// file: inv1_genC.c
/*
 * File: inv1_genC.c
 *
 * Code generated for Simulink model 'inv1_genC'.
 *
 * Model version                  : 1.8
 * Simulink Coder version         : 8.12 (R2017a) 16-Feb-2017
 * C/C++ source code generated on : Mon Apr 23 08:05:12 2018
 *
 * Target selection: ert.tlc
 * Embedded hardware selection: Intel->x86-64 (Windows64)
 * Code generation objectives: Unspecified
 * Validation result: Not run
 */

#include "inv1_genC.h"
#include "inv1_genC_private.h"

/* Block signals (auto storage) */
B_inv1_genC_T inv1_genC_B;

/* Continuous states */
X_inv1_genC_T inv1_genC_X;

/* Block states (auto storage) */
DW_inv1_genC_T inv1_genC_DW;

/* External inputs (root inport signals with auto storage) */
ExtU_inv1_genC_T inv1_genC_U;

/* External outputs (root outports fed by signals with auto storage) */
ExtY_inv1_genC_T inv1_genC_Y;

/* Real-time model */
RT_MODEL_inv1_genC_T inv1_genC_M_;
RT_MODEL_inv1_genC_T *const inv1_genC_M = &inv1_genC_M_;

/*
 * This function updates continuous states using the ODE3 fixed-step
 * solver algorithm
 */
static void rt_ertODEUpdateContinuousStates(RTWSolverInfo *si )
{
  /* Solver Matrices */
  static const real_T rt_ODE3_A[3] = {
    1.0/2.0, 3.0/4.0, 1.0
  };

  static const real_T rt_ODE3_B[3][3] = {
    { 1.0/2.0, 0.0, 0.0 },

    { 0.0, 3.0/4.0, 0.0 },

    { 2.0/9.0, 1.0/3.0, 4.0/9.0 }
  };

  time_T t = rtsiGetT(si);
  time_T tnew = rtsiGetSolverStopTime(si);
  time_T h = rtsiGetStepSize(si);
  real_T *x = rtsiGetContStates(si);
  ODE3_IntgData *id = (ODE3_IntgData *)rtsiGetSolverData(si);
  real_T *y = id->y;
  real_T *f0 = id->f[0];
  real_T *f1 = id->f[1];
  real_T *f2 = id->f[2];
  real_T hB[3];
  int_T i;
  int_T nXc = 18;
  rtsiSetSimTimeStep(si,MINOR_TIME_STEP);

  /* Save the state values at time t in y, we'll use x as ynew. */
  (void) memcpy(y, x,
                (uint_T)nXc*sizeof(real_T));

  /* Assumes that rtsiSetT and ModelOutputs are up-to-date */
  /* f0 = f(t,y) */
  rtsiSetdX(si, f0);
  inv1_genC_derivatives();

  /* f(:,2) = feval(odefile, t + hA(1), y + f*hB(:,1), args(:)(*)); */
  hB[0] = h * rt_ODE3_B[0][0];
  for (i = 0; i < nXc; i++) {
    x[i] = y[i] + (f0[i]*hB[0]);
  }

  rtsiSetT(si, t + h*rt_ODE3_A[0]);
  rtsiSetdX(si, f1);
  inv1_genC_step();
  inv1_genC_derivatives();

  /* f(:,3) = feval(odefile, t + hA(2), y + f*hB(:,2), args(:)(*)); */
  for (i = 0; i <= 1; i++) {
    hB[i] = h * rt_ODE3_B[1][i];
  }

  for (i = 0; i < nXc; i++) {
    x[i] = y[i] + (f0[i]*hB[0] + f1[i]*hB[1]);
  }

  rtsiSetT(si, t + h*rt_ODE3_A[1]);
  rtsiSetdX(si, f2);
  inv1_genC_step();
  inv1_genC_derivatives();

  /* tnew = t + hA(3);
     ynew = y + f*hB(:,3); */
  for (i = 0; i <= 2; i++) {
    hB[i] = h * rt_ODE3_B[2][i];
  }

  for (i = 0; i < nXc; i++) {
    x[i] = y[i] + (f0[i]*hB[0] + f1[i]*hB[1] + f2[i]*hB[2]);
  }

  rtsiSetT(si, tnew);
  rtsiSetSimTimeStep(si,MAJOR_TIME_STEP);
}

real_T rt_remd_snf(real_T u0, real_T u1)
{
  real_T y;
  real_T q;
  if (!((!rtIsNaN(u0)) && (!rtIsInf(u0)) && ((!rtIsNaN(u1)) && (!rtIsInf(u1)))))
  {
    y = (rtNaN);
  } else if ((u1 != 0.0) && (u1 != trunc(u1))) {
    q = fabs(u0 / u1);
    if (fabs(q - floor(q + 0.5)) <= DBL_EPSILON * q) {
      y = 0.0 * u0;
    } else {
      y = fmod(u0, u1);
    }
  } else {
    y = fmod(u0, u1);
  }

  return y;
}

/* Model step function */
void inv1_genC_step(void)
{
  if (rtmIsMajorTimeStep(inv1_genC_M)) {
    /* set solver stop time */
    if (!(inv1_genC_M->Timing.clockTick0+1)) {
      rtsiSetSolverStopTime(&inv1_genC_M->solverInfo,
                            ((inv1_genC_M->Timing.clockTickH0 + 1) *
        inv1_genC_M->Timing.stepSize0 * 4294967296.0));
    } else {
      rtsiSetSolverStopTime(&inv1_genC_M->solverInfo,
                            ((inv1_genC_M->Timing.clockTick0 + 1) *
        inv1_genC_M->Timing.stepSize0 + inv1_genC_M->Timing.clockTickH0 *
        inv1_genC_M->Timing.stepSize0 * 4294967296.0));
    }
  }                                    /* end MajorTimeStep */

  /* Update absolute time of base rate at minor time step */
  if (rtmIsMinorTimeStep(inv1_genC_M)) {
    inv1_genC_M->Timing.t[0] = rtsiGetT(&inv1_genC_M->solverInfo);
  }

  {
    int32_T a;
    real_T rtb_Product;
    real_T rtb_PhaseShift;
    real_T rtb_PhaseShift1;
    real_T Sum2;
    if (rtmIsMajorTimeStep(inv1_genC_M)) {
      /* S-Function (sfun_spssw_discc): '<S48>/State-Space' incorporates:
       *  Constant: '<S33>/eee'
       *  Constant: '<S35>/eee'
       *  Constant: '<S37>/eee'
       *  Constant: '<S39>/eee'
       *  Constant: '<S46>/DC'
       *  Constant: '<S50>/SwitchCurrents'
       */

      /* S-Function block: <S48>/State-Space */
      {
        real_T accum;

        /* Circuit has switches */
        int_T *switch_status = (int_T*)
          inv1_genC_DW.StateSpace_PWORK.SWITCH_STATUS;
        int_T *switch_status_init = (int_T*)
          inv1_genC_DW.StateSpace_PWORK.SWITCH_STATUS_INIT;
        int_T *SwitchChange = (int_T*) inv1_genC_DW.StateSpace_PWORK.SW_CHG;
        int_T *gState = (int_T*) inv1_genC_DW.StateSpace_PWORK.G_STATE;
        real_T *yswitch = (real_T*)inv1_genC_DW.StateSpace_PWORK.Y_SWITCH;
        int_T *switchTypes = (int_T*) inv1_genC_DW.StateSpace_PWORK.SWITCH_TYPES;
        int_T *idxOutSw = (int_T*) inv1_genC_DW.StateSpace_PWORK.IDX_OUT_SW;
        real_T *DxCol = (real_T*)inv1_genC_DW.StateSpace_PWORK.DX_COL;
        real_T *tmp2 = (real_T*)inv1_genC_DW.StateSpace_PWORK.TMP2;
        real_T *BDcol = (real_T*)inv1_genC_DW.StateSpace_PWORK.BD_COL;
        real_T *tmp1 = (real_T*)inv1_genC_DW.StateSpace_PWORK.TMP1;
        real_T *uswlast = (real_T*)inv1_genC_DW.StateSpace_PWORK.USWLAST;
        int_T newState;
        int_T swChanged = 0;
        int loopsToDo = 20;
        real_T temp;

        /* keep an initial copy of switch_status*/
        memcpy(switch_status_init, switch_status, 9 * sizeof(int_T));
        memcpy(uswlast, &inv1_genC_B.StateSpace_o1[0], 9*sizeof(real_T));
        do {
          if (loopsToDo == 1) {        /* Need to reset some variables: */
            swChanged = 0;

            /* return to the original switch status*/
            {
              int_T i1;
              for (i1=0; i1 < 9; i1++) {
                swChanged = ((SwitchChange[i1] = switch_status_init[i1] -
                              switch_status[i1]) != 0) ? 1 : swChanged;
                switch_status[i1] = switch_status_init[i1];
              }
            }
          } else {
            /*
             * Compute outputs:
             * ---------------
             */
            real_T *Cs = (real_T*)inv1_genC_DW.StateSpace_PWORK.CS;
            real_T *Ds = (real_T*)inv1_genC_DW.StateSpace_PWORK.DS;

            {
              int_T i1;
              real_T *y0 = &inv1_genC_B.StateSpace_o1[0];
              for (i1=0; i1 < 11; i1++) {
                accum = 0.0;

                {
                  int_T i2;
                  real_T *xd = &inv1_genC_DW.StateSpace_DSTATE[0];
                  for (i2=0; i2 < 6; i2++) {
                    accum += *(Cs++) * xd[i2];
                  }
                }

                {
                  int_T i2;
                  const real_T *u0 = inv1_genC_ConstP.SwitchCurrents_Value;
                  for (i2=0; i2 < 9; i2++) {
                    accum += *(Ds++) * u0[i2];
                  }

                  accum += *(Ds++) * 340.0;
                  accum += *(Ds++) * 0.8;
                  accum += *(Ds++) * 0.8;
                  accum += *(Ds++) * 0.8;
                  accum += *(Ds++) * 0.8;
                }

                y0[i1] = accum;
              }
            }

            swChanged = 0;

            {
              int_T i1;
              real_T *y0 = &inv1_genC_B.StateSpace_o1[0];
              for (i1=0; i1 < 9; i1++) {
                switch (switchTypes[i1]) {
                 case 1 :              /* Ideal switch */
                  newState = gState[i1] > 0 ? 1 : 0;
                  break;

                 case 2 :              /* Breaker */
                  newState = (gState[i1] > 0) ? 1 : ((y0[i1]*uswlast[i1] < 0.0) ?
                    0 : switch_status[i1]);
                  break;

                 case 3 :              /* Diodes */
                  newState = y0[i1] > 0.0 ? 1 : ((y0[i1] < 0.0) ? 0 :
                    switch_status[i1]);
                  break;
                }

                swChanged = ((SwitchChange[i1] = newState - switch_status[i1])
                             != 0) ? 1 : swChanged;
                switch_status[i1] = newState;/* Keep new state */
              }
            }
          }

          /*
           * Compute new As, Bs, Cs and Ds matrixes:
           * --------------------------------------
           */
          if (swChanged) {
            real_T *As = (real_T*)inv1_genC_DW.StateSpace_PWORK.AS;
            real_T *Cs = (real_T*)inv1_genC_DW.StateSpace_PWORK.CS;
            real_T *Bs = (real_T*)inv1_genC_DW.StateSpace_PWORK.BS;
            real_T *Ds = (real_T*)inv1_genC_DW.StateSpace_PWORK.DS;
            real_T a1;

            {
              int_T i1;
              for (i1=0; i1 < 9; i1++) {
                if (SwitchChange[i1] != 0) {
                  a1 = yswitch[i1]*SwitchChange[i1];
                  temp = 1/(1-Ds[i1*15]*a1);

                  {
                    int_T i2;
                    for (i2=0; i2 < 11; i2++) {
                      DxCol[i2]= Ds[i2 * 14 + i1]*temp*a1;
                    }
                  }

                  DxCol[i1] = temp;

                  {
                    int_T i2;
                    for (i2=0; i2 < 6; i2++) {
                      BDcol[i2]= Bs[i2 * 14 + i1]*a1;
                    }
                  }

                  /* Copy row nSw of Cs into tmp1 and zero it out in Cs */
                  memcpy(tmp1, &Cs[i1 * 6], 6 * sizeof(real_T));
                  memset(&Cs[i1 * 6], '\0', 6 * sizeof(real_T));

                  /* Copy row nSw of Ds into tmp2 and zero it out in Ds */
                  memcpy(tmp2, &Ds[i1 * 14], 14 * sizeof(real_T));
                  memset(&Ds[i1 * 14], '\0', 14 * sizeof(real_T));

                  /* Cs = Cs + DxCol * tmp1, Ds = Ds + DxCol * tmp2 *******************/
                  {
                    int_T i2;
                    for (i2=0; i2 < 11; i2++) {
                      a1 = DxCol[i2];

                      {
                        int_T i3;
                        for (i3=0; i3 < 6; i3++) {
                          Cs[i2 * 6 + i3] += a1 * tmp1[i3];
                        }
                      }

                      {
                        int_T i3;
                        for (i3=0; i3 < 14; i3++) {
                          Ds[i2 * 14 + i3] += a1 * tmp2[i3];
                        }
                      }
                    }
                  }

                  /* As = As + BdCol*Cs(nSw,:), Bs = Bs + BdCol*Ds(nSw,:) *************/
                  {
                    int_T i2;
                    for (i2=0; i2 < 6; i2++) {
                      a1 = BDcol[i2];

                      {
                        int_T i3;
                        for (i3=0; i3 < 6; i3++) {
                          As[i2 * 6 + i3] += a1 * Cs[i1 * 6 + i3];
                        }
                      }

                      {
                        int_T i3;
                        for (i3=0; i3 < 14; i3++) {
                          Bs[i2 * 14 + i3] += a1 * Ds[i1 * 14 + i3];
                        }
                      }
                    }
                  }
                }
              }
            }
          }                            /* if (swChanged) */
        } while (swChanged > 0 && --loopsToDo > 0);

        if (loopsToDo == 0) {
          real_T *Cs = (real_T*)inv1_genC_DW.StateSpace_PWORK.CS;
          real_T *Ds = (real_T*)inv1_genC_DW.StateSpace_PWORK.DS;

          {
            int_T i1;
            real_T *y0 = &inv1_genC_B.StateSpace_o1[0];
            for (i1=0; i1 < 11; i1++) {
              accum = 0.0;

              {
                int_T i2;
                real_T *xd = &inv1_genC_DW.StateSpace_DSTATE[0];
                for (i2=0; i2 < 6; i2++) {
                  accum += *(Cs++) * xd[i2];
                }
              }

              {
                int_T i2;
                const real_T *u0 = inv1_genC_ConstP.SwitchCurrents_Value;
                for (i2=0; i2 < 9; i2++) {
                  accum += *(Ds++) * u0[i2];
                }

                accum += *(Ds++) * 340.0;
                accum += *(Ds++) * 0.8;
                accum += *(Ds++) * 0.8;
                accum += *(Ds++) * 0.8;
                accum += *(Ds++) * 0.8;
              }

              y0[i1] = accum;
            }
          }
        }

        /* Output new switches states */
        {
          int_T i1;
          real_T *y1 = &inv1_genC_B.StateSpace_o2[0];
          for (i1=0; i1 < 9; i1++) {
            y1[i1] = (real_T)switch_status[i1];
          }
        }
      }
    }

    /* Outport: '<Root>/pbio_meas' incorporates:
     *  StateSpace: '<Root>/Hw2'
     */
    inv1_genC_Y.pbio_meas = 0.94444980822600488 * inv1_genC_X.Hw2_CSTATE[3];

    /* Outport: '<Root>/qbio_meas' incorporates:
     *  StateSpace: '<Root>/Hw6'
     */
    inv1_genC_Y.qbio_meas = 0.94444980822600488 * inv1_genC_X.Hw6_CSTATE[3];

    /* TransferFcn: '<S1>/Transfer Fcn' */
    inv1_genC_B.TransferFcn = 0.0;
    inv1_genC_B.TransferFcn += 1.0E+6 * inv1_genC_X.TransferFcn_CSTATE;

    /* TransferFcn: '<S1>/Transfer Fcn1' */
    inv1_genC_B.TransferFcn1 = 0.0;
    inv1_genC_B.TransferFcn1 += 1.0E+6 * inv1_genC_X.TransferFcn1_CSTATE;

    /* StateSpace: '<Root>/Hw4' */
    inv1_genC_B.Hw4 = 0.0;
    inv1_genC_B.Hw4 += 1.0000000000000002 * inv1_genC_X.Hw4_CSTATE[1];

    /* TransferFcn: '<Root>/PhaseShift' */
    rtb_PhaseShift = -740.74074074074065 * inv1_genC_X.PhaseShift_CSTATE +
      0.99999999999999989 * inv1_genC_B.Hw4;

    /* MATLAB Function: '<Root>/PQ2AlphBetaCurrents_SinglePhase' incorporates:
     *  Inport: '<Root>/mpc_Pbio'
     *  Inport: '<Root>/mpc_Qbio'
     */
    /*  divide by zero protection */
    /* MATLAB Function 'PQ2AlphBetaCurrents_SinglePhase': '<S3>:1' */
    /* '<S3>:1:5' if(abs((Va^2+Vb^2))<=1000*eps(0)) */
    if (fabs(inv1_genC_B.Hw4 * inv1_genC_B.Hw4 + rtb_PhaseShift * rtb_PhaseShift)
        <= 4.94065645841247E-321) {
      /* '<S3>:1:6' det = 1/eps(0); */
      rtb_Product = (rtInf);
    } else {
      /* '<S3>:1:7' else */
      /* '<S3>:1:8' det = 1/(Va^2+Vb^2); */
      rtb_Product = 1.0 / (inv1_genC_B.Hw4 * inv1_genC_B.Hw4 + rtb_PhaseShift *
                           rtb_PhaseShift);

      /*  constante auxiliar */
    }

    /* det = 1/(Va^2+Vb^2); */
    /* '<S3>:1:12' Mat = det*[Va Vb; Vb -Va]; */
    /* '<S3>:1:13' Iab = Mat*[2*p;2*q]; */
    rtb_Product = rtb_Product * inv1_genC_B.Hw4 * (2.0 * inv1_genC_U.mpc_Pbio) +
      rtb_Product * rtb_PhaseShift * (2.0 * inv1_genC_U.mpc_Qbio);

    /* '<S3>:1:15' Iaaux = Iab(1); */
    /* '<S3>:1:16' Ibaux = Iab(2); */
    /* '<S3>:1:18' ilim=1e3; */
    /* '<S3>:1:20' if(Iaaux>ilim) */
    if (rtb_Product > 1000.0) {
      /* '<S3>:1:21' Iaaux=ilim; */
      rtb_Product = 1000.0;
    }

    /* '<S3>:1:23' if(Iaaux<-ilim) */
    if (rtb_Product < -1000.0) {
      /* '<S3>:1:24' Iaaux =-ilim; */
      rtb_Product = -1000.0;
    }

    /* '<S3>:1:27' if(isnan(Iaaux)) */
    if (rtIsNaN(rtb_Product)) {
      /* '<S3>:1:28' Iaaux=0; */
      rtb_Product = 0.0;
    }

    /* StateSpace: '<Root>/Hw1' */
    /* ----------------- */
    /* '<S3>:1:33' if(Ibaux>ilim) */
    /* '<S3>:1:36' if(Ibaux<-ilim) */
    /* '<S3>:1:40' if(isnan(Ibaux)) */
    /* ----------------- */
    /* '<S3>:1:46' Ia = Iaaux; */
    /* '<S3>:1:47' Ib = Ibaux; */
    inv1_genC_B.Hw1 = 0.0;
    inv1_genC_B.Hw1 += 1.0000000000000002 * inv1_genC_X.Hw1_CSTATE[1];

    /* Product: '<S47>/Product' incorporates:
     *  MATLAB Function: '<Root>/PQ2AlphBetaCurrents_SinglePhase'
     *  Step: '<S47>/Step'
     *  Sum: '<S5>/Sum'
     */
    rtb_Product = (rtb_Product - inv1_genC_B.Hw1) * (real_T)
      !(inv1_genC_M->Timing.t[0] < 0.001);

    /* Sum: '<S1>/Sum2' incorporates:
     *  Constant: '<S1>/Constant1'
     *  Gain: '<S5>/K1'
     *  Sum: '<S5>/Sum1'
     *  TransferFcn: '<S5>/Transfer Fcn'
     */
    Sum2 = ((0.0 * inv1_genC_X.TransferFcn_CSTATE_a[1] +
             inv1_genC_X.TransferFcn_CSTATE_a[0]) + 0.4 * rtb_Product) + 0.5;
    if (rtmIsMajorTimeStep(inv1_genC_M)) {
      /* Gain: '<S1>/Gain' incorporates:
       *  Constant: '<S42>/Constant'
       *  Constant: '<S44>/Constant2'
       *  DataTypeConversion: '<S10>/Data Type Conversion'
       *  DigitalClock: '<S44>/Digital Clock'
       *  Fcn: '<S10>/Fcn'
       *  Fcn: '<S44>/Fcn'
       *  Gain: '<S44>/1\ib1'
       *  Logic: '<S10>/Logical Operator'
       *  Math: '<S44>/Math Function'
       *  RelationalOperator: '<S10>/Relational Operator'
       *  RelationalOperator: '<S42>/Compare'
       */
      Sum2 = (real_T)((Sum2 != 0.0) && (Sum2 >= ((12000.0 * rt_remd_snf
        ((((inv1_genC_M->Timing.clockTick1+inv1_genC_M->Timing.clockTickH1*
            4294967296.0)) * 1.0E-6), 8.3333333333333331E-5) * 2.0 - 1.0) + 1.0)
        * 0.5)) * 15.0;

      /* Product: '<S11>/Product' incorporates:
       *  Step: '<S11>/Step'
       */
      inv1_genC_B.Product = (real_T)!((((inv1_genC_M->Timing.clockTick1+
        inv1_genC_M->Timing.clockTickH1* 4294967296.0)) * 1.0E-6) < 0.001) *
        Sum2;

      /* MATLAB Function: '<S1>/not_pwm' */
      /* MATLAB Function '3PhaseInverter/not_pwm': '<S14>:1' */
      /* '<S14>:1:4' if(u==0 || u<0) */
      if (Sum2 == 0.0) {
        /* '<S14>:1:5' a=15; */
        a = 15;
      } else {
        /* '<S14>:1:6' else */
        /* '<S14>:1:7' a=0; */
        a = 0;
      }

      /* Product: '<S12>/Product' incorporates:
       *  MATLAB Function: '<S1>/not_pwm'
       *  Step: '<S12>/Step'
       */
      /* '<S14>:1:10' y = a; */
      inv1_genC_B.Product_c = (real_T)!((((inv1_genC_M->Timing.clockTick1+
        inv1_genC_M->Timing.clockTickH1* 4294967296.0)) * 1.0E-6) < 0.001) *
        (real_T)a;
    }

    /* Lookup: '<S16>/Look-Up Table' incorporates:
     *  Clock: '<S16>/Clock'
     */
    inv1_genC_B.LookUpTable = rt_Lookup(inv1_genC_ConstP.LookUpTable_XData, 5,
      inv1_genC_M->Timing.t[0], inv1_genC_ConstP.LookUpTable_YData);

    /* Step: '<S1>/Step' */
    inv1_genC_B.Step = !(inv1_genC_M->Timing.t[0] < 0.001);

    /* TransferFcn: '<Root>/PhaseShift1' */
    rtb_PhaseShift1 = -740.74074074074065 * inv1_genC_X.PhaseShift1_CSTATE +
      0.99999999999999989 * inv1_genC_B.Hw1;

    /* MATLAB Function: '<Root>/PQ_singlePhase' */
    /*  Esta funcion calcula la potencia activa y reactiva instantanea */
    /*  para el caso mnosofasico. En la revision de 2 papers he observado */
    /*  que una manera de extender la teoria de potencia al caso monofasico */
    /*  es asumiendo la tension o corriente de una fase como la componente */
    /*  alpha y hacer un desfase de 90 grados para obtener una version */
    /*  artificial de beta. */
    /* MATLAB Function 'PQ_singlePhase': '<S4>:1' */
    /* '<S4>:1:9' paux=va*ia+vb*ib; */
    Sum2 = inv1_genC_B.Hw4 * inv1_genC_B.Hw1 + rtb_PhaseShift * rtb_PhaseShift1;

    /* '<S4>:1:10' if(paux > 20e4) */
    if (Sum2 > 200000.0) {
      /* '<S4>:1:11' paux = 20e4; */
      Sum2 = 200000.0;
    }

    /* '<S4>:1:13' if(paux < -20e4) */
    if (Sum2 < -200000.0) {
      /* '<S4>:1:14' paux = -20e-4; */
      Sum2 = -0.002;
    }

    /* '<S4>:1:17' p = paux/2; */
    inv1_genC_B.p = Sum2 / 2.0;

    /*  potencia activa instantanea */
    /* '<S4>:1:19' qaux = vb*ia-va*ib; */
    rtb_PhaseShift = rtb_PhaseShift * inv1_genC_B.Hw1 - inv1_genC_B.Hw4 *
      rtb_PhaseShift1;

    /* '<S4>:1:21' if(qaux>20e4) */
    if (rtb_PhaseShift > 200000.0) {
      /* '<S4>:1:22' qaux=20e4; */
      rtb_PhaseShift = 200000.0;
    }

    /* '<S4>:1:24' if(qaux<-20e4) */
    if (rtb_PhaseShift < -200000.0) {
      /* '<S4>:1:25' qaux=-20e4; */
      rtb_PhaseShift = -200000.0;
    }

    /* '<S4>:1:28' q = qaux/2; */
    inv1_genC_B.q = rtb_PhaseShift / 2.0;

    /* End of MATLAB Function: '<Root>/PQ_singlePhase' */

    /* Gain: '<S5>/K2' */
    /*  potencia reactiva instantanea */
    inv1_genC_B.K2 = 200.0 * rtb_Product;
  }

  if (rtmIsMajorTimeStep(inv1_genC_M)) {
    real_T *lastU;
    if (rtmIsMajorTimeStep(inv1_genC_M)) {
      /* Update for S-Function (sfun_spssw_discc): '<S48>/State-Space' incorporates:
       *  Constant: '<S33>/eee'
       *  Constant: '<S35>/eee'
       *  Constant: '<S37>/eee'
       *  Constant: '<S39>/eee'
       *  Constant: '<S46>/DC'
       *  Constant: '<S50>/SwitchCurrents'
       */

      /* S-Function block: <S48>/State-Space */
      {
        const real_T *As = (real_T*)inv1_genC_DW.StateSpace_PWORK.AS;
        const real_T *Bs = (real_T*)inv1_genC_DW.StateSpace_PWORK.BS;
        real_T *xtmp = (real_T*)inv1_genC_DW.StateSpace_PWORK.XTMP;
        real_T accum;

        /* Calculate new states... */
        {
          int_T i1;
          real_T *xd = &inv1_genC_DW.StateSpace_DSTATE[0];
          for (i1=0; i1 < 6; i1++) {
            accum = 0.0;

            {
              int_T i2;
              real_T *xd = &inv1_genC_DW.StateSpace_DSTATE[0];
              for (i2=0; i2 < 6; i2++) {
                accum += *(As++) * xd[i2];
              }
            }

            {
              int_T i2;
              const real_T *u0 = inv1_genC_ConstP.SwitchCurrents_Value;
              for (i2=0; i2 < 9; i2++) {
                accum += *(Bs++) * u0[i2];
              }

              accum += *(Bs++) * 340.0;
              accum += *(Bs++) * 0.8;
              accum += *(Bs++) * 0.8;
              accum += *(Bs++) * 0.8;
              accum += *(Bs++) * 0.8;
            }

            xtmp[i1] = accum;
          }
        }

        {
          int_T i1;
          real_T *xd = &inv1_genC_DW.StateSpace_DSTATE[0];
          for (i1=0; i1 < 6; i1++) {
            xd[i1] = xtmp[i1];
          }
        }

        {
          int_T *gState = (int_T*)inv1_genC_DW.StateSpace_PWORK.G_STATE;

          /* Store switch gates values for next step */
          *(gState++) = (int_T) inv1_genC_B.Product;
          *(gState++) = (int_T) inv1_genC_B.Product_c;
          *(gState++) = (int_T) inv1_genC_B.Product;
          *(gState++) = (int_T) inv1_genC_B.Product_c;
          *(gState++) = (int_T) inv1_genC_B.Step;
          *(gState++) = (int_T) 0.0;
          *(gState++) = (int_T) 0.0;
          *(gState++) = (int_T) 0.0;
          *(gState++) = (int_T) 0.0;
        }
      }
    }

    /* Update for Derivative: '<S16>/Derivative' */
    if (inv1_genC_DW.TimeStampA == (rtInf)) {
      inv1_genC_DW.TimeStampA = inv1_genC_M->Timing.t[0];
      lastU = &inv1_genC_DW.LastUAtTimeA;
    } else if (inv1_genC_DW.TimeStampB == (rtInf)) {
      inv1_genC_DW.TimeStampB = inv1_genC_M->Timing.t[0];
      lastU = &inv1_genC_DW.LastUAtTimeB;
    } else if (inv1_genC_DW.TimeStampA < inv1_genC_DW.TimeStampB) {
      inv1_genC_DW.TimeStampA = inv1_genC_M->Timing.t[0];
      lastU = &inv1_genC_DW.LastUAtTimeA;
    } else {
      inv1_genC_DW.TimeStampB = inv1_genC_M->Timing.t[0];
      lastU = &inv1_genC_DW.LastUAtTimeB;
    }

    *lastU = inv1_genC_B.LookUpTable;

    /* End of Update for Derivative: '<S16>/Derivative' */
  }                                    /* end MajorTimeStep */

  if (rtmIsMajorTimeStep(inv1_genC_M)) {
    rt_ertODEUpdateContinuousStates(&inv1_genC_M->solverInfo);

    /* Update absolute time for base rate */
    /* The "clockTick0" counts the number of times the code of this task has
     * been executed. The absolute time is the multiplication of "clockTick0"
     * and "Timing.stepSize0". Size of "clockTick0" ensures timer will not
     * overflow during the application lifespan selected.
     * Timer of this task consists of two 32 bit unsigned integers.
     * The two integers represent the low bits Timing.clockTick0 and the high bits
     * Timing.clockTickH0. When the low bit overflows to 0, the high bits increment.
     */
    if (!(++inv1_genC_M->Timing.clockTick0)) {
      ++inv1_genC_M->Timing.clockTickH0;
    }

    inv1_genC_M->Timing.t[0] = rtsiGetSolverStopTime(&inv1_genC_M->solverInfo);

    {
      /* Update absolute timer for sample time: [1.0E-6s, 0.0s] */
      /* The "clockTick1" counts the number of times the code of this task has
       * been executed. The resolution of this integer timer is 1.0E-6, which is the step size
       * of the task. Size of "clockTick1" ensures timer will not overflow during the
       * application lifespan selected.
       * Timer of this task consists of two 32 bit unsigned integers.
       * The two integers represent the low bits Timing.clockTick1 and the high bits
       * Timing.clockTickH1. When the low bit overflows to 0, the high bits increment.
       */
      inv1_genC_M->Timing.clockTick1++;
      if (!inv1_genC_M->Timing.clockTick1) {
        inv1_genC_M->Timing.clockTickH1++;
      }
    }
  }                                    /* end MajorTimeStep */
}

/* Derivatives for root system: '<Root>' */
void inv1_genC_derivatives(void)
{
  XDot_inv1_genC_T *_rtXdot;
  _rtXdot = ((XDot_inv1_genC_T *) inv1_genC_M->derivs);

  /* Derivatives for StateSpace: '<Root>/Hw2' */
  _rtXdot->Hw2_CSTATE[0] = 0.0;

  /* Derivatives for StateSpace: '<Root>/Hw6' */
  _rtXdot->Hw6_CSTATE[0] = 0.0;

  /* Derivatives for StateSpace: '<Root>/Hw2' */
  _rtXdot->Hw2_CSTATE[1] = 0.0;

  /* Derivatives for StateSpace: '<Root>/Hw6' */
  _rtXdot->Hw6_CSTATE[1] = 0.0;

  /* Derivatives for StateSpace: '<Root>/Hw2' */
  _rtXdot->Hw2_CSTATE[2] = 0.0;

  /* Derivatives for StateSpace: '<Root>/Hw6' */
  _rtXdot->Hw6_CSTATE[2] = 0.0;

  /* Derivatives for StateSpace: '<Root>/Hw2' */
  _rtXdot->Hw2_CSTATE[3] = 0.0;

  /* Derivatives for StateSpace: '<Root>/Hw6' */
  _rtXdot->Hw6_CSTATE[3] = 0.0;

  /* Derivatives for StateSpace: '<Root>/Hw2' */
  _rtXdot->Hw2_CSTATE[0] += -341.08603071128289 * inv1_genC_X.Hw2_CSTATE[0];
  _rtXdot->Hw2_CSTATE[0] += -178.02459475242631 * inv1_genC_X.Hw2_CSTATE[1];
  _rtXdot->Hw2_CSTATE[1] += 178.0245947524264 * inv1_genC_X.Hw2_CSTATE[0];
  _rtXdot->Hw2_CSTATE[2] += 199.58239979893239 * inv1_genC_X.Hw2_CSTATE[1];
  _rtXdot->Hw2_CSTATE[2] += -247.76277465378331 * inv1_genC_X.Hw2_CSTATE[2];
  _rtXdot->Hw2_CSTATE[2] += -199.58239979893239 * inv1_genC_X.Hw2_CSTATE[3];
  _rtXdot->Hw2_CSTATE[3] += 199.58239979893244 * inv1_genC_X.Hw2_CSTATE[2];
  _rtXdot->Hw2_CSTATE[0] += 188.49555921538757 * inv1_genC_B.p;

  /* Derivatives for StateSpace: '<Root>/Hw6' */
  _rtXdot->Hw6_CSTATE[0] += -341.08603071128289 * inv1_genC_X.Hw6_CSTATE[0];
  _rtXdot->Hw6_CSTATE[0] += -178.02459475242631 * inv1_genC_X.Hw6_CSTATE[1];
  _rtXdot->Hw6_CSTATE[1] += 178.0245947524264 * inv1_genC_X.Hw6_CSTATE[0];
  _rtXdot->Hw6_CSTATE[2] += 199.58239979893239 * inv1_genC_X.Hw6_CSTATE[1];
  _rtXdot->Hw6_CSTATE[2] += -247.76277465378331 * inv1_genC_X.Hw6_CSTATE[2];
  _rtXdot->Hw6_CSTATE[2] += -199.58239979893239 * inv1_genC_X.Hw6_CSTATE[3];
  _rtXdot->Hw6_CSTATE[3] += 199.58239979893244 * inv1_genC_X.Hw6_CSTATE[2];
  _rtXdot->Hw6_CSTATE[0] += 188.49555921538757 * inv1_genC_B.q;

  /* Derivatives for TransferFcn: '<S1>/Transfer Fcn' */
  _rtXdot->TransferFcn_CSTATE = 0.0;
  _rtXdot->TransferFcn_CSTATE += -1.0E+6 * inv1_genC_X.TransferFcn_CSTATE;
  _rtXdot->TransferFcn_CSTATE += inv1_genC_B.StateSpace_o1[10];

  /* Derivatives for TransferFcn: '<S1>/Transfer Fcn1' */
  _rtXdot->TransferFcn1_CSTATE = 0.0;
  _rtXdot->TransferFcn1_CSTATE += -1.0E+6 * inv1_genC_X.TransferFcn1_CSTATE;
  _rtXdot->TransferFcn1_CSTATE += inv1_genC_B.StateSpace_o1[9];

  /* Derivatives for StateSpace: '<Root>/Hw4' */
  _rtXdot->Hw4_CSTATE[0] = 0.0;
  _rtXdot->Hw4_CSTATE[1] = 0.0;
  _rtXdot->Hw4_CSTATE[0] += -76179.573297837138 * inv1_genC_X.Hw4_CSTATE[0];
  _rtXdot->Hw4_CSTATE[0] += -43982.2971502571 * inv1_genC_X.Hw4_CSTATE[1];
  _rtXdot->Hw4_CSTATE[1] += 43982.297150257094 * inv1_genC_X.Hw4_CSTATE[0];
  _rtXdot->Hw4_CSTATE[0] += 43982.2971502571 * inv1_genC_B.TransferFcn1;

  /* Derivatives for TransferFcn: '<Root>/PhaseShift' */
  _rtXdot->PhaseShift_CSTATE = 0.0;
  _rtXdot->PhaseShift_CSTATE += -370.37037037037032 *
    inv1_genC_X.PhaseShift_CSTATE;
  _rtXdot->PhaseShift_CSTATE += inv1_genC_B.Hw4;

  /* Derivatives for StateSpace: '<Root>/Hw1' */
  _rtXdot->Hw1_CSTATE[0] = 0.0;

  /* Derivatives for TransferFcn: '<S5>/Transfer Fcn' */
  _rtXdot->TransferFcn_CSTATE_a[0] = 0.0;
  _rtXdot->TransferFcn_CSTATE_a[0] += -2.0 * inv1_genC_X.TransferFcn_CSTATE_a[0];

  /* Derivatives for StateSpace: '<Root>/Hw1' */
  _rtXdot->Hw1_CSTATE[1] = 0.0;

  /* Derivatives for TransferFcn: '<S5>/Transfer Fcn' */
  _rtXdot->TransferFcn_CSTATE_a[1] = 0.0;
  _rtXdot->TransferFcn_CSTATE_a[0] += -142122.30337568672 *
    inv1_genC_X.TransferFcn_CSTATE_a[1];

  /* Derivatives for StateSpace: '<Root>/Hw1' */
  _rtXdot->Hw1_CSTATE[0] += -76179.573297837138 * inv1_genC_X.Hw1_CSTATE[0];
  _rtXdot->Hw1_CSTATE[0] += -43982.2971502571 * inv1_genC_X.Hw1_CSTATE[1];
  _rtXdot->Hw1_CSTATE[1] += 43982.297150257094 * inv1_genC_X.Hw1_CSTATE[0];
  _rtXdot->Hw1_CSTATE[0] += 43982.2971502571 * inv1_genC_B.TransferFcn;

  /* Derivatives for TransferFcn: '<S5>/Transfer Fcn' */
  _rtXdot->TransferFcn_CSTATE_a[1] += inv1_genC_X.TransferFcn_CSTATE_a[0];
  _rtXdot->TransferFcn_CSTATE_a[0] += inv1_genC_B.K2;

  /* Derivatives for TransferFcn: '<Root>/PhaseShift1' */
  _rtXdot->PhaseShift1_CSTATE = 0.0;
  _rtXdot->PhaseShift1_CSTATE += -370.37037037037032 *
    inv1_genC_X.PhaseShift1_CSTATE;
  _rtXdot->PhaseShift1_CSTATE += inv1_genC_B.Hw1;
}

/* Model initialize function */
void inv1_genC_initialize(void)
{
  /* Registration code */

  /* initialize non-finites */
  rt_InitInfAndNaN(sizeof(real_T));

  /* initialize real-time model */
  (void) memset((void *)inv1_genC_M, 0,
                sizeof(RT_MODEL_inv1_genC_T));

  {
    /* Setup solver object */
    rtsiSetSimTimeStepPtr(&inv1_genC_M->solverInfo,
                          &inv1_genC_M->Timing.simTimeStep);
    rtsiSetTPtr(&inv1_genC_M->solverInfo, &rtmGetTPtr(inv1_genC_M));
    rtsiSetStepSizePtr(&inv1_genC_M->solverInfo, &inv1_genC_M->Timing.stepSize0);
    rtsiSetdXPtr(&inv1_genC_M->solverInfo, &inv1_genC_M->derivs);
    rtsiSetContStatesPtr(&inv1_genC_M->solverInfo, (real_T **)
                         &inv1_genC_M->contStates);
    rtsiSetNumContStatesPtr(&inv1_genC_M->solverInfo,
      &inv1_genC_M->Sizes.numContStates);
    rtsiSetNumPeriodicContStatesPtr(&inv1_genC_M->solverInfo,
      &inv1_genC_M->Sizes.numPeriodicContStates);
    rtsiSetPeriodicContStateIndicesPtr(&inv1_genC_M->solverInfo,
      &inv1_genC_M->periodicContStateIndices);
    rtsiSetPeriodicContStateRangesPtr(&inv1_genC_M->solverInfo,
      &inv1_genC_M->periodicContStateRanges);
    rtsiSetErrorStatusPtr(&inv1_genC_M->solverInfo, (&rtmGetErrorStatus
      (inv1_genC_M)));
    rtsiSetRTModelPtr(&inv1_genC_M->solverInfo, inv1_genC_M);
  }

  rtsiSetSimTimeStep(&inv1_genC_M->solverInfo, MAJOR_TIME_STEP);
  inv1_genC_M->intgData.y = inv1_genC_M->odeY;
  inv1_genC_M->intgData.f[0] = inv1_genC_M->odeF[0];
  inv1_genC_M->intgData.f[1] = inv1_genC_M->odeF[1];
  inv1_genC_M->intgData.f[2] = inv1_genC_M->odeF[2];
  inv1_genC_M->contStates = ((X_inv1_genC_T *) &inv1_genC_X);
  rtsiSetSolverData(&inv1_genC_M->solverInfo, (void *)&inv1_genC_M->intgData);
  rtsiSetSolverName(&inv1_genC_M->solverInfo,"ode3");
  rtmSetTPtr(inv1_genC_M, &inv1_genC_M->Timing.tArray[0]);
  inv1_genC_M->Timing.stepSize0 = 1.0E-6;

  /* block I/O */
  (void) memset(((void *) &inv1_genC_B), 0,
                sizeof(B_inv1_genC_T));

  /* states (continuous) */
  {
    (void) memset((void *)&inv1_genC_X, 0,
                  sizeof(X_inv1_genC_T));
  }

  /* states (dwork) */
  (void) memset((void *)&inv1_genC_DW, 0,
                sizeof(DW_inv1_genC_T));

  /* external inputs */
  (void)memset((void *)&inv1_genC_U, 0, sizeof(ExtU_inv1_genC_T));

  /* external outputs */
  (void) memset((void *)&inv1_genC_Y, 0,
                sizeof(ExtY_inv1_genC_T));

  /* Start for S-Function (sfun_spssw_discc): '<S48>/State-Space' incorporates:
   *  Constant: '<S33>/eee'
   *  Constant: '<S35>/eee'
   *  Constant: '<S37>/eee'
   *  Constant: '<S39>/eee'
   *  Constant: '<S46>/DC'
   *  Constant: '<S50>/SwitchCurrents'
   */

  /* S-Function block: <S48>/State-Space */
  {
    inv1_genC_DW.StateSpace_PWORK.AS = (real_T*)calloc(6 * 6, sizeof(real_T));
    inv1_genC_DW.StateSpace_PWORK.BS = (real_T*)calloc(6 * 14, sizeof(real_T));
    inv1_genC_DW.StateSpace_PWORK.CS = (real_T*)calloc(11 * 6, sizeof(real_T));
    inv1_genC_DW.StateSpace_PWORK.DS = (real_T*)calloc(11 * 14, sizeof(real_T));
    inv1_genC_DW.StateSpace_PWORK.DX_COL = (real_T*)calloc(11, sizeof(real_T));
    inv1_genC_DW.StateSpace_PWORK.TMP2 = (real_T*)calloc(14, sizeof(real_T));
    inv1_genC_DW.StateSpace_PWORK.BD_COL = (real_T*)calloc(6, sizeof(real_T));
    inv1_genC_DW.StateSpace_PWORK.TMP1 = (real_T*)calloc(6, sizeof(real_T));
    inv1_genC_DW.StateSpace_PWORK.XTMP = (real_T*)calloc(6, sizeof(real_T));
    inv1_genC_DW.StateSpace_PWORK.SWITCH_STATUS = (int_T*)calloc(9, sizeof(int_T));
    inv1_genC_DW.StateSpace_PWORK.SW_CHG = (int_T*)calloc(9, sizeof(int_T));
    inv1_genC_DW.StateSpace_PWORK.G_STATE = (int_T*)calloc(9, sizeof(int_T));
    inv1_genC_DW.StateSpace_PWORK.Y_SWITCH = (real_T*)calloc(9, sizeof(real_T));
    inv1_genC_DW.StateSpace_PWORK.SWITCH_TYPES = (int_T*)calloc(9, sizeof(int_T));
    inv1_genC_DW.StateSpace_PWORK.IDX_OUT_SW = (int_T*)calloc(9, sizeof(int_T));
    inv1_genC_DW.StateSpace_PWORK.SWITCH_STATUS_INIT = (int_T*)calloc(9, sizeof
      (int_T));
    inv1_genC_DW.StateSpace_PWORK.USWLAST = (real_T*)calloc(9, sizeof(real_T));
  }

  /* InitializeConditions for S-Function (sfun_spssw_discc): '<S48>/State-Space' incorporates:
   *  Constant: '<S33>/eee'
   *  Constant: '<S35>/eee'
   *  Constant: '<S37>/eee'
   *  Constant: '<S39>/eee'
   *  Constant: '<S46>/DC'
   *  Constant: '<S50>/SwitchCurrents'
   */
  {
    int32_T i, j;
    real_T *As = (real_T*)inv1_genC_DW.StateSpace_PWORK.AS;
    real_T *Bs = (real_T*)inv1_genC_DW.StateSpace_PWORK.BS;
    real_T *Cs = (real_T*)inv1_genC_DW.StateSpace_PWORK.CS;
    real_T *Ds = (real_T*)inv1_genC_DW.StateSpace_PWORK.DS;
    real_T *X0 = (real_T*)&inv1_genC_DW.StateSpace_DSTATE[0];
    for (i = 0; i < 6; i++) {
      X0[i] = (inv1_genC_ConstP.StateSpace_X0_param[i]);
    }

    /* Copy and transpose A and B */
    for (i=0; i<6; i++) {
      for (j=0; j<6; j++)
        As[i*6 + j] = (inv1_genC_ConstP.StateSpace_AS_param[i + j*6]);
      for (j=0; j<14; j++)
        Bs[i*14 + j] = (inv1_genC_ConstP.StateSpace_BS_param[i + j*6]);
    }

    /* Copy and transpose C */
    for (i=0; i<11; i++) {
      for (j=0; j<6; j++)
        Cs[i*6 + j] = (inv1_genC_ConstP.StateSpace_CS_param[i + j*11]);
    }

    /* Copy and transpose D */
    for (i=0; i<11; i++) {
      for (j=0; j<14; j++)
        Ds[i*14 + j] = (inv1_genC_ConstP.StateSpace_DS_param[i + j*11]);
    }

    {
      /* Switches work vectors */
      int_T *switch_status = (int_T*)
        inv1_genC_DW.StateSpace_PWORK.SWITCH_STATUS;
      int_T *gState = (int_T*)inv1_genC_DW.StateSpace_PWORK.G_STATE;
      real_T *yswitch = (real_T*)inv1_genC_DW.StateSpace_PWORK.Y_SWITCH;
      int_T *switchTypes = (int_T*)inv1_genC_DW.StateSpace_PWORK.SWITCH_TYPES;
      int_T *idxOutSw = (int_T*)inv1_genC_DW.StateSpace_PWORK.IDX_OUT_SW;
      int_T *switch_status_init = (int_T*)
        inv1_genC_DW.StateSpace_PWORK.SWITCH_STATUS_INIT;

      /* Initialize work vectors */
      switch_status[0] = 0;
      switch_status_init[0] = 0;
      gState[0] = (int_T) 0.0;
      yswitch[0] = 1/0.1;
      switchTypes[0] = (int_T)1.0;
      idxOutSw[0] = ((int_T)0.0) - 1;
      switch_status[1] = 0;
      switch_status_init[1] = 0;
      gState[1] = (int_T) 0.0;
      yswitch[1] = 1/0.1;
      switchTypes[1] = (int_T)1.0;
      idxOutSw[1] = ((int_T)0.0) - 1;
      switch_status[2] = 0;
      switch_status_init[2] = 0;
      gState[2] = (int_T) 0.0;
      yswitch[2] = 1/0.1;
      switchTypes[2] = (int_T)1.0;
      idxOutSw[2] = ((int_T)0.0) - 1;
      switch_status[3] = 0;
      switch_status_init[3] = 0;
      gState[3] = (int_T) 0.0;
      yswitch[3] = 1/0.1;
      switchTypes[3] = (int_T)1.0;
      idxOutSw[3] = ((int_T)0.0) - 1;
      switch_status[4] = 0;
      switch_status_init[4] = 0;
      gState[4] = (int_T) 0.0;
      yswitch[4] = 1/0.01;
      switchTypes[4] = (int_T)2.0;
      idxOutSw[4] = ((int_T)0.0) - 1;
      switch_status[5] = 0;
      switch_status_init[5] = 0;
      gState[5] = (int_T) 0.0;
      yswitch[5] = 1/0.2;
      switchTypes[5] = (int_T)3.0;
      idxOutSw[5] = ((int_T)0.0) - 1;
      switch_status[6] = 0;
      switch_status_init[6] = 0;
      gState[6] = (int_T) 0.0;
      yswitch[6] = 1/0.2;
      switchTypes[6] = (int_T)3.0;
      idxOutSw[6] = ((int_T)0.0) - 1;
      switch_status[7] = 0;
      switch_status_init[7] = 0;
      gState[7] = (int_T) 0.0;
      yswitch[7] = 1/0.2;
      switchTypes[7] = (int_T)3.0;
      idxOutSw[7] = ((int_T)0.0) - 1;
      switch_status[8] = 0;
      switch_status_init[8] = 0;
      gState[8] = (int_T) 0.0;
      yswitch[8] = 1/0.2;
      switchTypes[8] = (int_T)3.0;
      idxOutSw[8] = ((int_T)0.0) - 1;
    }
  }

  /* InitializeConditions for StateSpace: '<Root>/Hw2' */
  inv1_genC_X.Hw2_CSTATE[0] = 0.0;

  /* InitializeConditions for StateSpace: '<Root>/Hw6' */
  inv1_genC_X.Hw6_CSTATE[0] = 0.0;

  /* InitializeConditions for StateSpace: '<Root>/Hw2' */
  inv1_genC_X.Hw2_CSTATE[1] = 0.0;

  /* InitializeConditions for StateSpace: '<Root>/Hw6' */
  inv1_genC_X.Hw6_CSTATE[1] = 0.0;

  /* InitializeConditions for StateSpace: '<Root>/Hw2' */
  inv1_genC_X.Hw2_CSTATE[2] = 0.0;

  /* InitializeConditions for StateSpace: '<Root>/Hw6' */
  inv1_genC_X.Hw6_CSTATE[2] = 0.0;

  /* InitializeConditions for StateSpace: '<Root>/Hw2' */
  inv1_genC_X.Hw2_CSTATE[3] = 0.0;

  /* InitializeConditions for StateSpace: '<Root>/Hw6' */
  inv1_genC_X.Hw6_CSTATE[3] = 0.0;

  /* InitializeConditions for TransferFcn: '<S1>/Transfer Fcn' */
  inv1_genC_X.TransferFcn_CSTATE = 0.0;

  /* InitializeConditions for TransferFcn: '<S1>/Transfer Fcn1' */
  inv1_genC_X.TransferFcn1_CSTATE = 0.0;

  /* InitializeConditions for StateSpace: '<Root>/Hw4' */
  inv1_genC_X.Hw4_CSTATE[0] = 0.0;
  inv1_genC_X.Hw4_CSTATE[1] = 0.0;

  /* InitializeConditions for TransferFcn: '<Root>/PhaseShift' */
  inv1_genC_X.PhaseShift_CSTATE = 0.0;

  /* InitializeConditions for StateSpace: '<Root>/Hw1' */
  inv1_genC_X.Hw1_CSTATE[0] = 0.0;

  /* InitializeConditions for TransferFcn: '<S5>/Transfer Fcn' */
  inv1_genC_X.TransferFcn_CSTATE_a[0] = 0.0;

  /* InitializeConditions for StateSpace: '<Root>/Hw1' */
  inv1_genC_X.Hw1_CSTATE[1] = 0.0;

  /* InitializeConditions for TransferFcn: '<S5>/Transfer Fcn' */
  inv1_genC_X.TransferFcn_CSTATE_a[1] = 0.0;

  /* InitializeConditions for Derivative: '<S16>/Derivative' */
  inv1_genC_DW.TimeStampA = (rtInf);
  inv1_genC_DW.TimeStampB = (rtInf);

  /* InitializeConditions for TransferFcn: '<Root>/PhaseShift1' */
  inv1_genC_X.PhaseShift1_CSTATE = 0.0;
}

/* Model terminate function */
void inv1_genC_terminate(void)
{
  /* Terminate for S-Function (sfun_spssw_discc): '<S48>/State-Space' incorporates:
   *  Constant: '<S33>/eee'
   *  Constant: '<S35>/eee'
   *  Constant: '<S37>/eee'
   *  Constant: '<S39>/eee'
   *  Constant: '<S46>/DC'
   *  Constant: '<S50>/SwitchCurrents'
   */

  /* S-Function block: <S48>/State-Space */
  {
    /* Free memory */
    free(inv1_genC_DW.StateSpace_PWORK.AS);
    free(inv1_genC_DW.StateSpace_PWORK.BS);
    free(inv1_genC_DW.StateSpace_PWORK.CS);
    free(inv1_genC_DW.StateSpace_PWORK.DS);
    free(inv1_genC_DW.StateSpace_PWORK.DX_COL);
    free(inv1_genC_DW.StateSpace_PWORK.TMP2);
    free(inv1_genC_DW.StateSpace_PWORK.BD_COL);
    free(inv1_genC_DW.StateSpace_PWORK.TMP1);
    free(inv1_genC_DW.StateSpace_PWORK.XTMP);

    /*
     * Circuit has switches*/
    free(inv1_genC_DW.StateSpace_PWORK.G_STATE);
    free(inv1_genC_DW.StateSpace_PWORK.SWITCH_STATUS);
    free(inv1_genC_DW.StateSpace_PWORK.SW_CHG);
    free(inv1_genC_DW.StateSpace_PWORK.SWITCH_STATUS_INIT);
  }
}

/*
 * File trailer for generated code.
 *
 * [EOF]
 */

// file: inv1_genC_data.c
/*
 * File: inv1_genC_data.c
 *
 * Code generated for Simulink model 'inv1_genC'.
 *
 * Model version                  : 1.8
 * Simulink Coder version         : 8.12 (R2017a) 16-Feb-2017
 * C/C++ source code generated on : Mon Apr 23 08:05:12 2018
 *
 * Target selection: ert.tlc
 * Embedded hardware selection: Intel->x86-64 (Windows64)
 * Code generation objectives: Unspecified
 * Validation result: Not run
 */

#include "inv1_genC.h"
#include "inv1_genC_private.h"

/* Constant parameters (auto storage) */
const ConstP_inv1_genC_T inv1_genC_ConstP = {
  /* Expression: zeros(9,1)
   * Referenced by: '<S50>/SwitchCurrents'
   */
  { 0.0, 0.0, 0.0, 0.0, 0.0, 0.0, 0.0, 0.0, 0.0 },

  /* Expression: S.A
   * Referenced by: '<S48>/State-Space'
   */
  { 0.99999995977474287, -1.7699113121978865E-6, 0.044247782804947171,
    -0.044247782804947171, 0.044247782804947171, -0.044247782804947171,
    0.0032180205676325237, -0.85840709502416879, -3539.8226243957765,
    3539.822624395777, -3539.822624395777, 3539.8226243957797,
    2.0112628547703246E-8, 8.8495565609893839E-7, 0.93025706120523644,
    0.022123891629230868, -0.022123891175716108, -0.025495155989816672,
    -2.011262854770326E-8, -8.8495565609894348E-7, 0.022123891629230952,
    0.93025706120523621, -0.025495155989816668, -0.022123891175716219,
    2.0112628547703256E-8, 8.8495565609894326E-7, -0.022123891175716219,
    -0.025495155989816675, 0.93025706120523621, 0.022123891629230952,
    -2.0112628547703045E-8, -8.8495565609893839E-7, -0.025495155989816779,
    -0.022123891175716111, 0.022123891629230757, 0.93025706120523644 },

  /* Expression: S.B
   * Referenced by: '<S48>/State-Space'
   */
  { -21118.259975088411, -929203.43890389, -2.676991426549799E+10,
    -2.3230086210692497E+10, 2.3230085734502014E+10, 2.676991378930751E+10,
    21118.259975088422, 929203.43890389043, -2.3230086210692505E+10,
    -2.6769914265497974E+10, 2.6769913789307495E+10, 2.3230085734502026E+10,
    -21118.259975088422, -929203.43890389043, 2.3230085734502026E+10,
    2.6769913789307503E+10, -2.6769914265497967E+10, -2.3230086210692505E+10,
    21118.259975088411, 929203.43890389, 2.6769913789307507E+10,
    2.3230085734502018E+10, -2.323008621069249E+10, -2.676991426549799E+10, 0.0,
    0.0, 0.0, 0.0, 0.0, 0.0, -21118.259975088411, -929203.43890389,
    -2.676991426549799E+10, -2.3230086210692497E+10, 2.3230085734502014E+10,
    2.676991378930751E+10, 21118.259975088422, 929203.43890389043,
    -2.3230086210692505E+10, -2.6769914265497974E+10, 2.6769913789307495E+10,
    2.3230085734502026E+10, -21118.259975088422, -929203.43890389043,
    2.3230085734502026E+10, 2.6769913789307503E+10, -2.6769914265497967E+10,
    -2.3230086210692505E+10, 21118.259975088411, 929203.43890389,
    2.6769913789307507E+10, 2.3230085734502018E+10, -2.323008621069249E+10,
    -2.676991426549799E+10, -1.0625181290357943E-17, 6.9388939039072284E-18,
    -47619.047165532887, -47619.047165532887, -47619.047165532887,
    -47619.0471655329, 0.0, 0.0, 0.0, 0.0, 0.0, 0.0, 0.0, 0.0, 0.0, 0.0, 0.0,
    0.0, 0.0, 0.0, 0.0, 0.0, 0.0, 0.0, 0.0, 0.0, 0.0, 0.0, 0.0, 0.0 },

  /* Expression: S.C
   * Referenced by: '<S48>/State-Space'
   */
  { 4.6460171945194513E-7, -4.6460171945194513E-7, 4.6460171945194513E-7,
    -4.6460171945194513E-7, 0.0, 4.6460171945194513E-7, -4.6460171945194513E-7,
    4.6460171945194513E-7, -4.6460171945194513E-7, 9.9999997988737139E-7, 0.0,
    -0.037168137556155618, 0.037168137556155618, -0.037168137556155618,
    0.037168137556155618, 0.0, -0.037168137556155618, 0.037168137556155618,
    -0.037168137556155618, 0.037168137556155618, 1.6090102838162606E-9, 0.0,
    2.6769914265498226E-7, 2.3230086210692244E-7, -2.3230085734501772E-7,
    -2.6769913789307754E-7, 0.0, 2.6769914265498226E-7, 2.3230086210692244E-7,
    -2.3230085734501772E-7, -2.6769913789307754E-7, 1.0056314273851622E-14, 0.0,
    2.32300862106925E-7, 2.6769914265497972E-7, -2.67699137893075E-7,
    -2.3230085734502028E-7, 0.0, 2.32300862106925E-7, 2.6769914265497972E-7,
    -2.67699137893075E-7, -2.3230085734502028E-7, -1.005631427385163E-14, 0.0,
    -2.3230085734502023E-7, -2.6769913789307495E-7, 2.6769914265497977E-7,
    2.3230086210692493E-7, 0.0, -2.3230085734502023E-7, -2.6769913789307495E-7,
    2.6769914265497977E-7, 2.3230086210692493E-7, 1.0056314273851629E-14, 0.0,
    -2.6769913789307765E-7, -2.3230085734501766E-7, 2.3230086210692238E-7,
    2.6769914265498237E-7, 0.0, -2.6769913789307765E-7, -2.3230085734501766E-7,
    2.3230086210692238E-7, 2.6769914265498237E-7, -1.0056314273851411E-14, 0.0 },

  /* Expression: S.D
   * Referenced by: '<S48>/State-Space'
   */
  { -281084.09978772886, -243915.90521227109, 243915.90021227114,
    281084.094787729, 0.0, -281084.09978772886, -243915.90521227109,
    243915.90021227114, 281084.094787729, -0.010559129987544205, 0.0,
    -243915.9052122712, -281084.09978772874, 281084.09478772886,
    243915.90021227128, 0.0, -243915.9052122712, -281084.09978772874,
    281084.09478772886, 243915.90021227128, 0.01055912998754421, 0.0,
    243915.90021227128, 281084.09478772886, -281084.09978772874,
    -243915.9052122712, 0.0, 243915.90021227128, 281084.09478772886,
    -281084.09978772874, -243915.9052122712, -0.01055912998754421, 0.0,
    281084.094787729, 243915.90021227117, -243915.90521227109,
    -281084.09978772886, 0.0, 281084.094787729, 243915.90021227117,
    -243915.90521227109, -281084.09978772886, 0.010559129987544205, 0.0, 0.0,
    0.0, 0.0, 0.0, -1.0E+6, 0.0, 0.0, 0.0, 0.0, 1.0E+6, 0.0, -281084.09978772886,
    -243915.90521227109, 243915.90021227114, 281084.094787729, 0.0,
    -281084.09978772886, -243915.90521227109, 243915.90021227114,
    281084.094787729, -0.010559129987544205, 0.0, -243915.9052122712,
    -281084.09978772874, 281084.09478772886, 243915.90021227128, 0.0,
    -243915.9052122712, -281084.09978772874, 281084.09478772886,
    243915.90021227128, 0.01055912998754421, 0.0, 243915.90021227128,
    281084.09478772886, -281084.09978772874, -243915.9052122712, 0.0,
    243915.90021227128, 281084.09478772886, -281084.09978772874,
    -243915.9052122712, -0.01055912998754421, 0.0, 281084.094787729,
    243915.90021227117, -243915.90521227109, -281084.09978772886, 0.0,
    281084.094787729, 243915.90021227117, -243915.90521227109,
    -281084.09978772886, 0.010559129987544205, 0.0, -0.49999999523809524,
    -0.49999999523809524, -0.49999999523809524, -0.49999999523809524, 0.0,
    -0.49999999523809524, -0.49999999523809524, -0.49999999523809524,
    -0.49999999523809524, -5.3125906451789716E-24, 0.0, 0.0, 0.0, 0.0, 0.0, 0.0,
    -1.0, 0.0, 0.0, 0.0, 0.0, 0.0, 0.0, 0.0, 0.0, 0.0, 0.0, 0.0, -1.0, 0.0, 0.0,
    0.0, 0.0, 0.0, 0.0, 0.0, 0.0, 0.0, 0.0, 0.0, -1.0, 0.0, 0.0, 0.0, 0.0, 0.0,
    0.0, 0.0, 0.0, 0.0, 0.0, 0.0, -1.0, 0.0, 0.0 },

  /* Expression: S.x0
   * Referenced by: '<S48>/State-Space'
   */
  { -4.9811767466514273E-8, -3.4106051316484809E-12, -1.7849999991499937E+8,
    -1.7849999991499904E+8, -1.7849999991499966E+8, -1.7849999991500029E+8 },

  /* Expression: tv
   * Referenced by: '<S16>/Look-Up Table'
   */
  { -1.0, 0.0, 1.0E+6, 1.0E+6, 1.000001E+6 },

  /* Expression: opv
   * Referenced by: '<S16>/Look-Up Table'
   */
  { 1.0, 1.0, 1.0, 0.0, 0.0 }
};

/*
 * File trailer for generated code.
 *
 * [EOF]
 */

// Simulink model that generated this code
simulink model "inv1_genC"  (R2017a)
settings: Solver=ode3  StartTime=0.0  StopTime=10.0  FixedStep=1e-6  RelTol=1e-3
libraries: powerlib x17, dsparch4 x4, powerlib_meascontrol x1

== system inv1_genC ==
  note: BIO - CSI
  mpc_Pbio : Inport
  mpc_Qbio : Inport  Port=2
  3PhaseInverter : Subsystem  mask{st_time=1e-3, f_sw=12000, samp_f=1e-6}
      mask prompts: st_time "Tiempo muerto (Start)"; f_sw "Switching frequency"; samp_f "samplig"
  DC 340V : powerlib/Electrical Sources/DC Voltage Source  Amplitude=340  Measurements=None
  Ground1 : powerlib/Elements/Ground  LConnTagsString=a
  Hw1 : dsparch4/Analog Filter Design  method=Bessel  filttype=Lowpass  N=2  Wlo=7000*2*pi  Whi=80  Rp=2  Rs=80
  Hw2 : dsparch4/Analog Filter Design  method=Bessel  filttype=Lowpass  N=4  Wlo=30*2*pi  Whi=80  Rp=2  Rs=80
  Hw4 : dsparch4/Analog Filter Design  method=Bessel  filttype=Lowpass  N=2  Wlo=7000*2*pi  Whi=80  Rp=2  Rs=80
  Hw6 : dsparch4/Analog Filter Design  method=Bessel  filttype=Lowpass  N=4  Wlo=30*2*pi  Whi=80  Rp=2  Rs=80
  PQ2AlphBetaCurrents_SinglePhase : MATLAB Function  TreatAsAtomicUnit=on
  PQ_singlePhase : MATLAB Function  TreatAsAtomicUnit=on
  PR Controller_0_ref 3 : Subsystem  mask{Kp=40/100, Ki=200, wa=2, w0=60*2*pi, st_time=1e-3}
      mask prompts: Kp "Ganancia Proporcional"; Ki "Ganancia Integral"; wa "Ancho camapana resonancia"; w0 "Frecuencia Central"; st_time "Tiempo muerto (Start)"
  PhaseShift : TransferFcn  Numerator=[2.7e-3 -1]  Denominator=[2.7e-3 1]
  PhaseShift1 : TransferFcn  Numerator=[2.7e-3 -1]  Denominator=[2.7e-3 1]
  Rin : powerlib/Elements/Series RLC Branch  LConnTagsString=__new0  RConnTagsString=__new0  BranchType=R  Resistance=.01  Inductance=0  SetiL0=off  InitialCurrent=0  Capacitance=0  Setx0=off  InitialVoltage=0  Measurements=None
  powergui : powerlib/powergui  Priority=1  SimulationMode=Discrete  SampleTime=1e-6  frequency=60  Iterations=50  frequencyindice=0  Pbase=100e6  ErrMax=1e-4  UnitsV=kV  UnitsW=MW  buscounter=0  FunctionMessages=off  echomessages=off  EnableUseOfTLC=off  CurrentSourceSwitches=off  DisableSnubberDevices=off  DisableRonSwitches=off  DisableVfSwitches=off  DisplayEquations=off  SolverType=Tustin/Backward Euler (TBE)  Interpol=off  ExternalGateDelay=off  methode=off  Ts=100  x0status=blocks  SPID=off  SwTol=0  HookPort=off  RestoreLinks=warning  ResistiveCurrentMeasurement=off  Frange=[0:2:500]  Ylog=off  Xlog=on  ShowGrid=off  save=off  variable=ZData  structure=0  ZoomFFT=off  StartTime=0.0  cycles=1  DisplayStyle=1  fundamental=60  FreqAxis=off  MaxFrequency=1000  frequencyindicesteady=1  RmsSteady=1  display=off
  pbio_meas : Outport
  qbio_meas : Outport  Port=2
  wires:
  [V_bet_bio] -> PQ2AlphBetaCurrents_SinglePhase/2(Vb)
  [Ia_ref_bio] -> PR Controller_0_ref 3/1(ref)
  PQ2AlphBetaCurrents_SinglePhase/1(Ia) -> [Ia_ref_bio]
  3PhaseInverter/2(Vout) -> Hw4/1
  3PhaseInverter/1(Iout) -> Hw1/1
  PhaseShift/1 -> [V_bet_bio]
  PhaseShift1/1 -> [I_bet_bio]
  [I_bio] -> [I_alf_bio], PhaseShift1/1
  mpc_Pbio/1 -> PQ2AlphBetaCurrents_SinglePhase/3(p)
  Hw1/1 -> [I_bio]
  PR Controller_0_ref 3/1(Out1) -> [D_bio]
  [I_bio] -> PR Controller_0_ref 3/2(real)
  mpc_Qbio/1 -> PQ2AlphBetaCurrents_SinglePhase/4(q)
  Hw4/1 -> [V_bio]
  [D_bio] -> 3PhaseInverter/1(A_in)
  [V_alf_bio] -> PQ2AlphBetaCurrents_SinglePhase/1(Va)
  [V_bio] -> [V_alf_bio], PhaseShift/1
  Hw6/1 -> qbio_meas/1
  [V_bet_bio] -> PQ_singlePhase/2(vb)
  PQ_singlePhase/2(q) -> Hw6/1
  Hw2/1 -> pbio_meas/1
  [I_alf_bio] -> PQ_singlePhase/3(ia)
  PQ_singlePhase/1(p) -> Hw2/1
  [V_alf_bio] -> PQ_singlePhase/1(va)
  [I_bet_bio] -> PQ_singlePhase/4(ib)
  connections:
  DC 340V/RConn1 -- Rin/LConn1
  DC 340V/LConn1 -- 3PhaseInverter/LConn2
  3PhaseInverter/RConn2 -- Ground1/LConn1
  Rin/RConn1 -- 3PhaseInverter/LConn1

== system inv1_genC/3PhaseInverter ==
  note: Gate Drivers: Generan las señales cuadradas para la conmutacion del convertidor de 3 brazos e implementan el tiempo muerto para mejorar la calidad de la simulacion
  A_in : Inport
  Breaker : powerlib/Elements/Breaker  InitialState=0  SwitchingTimes="[1/60  5/60]"  External=on  BreakerResistance=0.01  SnubberResistance=1e6  SnubberCapacitance=inf  Measurements=None  MoreParameters=on  NoBreakLoop=off
  Cf : powerlib/Elements/Series RLC Branch  LConnTagsString=__new0  RConnTagsString=__new0  BranchType=C  Resistance=1  Inductance=1e-3  SetiL0=off  InitialCurrent=0  Capacitance=22e-6  Setx0=off  InitialVoltage=0  Measurements=None
  Constant1 : Constant  Value=0.5
  Gain : Gain  Gain=15
  H bridge : Subsystem
  I sens A : powerlib/Measurements/Current Measurement  PhasorSimulation=off  OutputType=Complex  PSBequivalent=0
  Lf : powerlib/Elements/Series RLC Branch  LConnTagsString=__new0  RConnTagsString=__new0  BranchType=RL  Resistance=.1  Inductance=40e-3  SetiL0=off  InitialCurrent=0  Capacitance=1e-6  Setx0=off  InitialVoltage=0  Measurements=None
  PWM Generator (DC-DC) : powerlib_meascontrol/Pulse & Signal Generators/PWM Generator (DC-DC)  Fsw=f_sw  Ts=samp_f
  Step : Step  Time=st_time  SampleTime=0
  Steper1 : Subsystem
  Steper3 : Subsystem
  Sum2 : Sum
  Transfer Fcn : TransferFcn  Denominator=[1e-6 1]
  Transfer Fcn1 : TransferFcn  Denominator=[1e-6 1]
  Vsensa1 : powerlib/Measurements/Voltage Measurement  PhasorSimulation=off  OutputType=Complex  PSBequivalent=0
  not_pwm : MATLAB Function  TreatAsAtomicUnit=on
  Vout+ : PMIOPort  Port=1  Side=Right
  Vout- : PMIOPort  Port=2  Side=Right
  Collector : PMIOPort  Port=3  Side=Left
  Emitter : PMIOPort  Port=4  Side=Left
  Iout : Outport
  Vout : Outport  Port=2
  wires:
  not_pwm/1(y) -> Steper3/1(In1)
  Sum2/1 -> PWM Generator (DC-DC)/1
  PWM Generator (DC-DC)/1 -> Gain/1
  Constant1/1 -> Sum2/2
  A_in/1 -> Sum2/1
  Steper1/1(Out1) -> [pwma]
  Steper3/1(Out1) -> [Npwma]
  Gain/1 -> Steper1/1(In1), not_pwm/1(u)
  [pwma] -> H bridge/1(Ahi)
  [Npwma] -> H bridge/2(Bhi), H bridge/3(Alo)
  [pwma] -> H bridge/4(Blo)
  I sens A/1 -> Transfer Fcn/1  "A_current"
  Vsensa1/1 -> Transfer Fcn1/1  "A_volts"
  Transfer Fcn/1 -> Iout/1
  Transfer Fcn1/1 -> Vout/1
  Step/1 -> Breaker/1
  connections:
  H bridge/RConn3 -- Collector/RConn1
  H bridge/RConn4 -- Emitter/RConn1
  Lf/LConn1 -- H bridge/RConn1
  H bridge/RConn2 -- Vsensa1/LConn2 -- Vout-/RConn1 -- Cf/RConn1
  Breaker/LConn1 -- I sens A/RConn1
  Breaker/RConn1 -- Vsensa1/LConn1 -- Vout+/RConn1
  Cf/LConn1 -- I sens A/LConn1 -- Lf/RConn1

== system inv1_genC/PR Controller_0_ref 3 ==
  ref : Inport
  real : Inport  Port=2
  K1 : Gain  Gain=Kp
  K2 : Gain  Gain=Ki
  Steper6 : Subsystem
  Sum : Sum  Inputs=+-
  Sum1 : Sum  Inputs=+|+
  Transfer Fcn : TransferFcn  Numerator=[1 0]  Denominator=[1 wa (w0)^2]
  Out1 : Outport
  wires:
  real/1 -> Sum/2
  ref/1 -> Sum/1
  Sum/1 -> Steper6/1(In1)
  K1/1 -> Sum1/1
  Transfer Fcn/1 -> Sum1/2
  K2/1 -> Transfer Fcn/1
  Steper6/1(Out1) -> K1/1, K2/1
  Sum1/1 -> Out1/1

== system inv1_genC/3PhaseInverter/H bridge ==
  note: Convertirdor de 3 brazos: Implementado usando interruptores ideales para agilizar la simulacion. la salida E correspone a la corriente y laa tension de cada componente (sea interruptor o diodo) y su respectiva corriente. no tienen puerto de salida ya que no son relevantes para lo que se desea simular. si g=0 interruptor no conduce. si g=1 interruptor conduce. conmutacion ocurre instantaneamente sin retardo.
  Ahi : Inport
  Bhi : Inport  Port=2
  Alo : Inport  Port=3
  Blo : Inport  Port=4
   sw_ahi{1..2,5..6} (4 alike) : powerlib/Power Electronics/Ideal Switch  Ron=0.1  Lon=0  IC=0  Rs=1e6  Cs=10e-12  Measurements=on
  Diode{1..3,6} (4 alike) : powerlib/Power Electronics/Diode  Ron=.2  Lon=0  Vf=0.8  IC=0  UseSnubber=0  Rs=0  Cs=0  Measurements=on
  " Vout+" : PMIOPort  Tag=PMCPort  Port=1  Side=Right
  Vout- : PMIOPort  Tag=PMCPort  Port=2  Side=Right
  Collector : PMIOPort  Tag=PMCPort  Port=3  Side=Right
  Emitter : PMIOPort  Tag=PMCPort  Port=4  Side=Right
  wires:
  Alo/1 -> " sw_ahi6"/1
  Ahi/1 -> " sw_ahi1"/1
  Blo/1 -> " sw_ahi5"/1
  Bhi/1 -> " sw_ahi2"/1
  connections:
  Diode3/RConn1 -- Vout-/RConn1 -- " sw_ahi2"/LConn1 -- Diode2/LConn1 -- " sw_ahi5"/RConn1
  Diode3/LConn1 -- Emitter/RConn1 -- Diode6/LConn1 -- " sw_ahi6"/LConn1 -- " sw_ahi5"/LConn1
  Diode2/RConn1 -- Collector/RConn1 -- " sw_ahi1"/RConn1 -- Diode1/RConn1 -- " sw_ahi2"/RConn1
  " sw_ahi6"/RConn1 -- Diode6/RConn1 -- " Vout+"/RConn1 -- Diode1/LConn1 -- " sw_ahi1"/LConn1

== system inv1_genC/3PhaseInverter/Steper1 ==
  In1 : Inport
  Product : Product
  Step : Step  Time=st_time  SampleTime=samp_f
  Out1 : Outport
  wires:
  Step/1 -> Product/2
  In1/1 -> Product/1
  Product/1 -> Out1/1

== system inv1_genC/3PhaseInverter/Steper3 ==
  In1 : Inport
  Product : Product
  Step : Step  Time=st_time  SampleTime=samp_f
  Out1 : Outport
  wires:
  Product/1 -> Out1/1
  In1/1 -> Product/1
  Step/1 -> Product/2

== system inv1_genC/PR Controller_0_ref 3/Steper6 ==
  In1 : Inport
  Product : Product
  Step : Step  Time=st_time  SampleTime=0
  Out1 : Outport
  wires:
  Product/1 -> Out1/1
  In1/1 -> Product/1
  Step/1 -> Product/2

== matlab function inv1_genC/3PhaseInverter/not_pwm ==
function y = fcn(u)
%#codegen

if(u==0 || u<0)
    a=15;
else
    a=0;
end;

y = a;

== matlab function inv1_genC/PQ_singlePhase ==
function [p, q] = fcn(va, vb, ia, ib)
% Esta funcion calcula la potencia activa y reactiva instantanea
% para el caso mnosofasico. En la revision de 2 papers he observado
% que una manera de extender la teoria de potencia al caso monofasico
% es asumiendo la tension o corriente de una fase como la componente
% alpha y hacer un desfase de 90 grados para obtener una version
% artificial de beta.

paux=va*ia+vb*ib;
if(paux > 20e4)
    paux = 20e4;
end
if(paux < -20e4)
    paux = -20e-4;
end

p = paux/2; % potencia activa instantanea

qaux = vb*ia-va*ib;

if(qaux>20e4)
    qaux=20e4;
end
if(qaux<-20e4)
    qaux=-20e4;
end

q = qaux/2; % potencia reactiva instantanea

== matlab function inv1_genC/PQ2AlphBetaCurrents_SinglePhase ==
function [Ia, Ib] = fcn(Va, Vb, p, q)
%#codegen

% divide by zero protection
if(abs((Va^2+Vb^2))<=1000*eps(0))
    det = 1/eps(0);
else
    det = 1/(Va^2+Vb^2); % constante auxiliar
end;
%det = 1/(Va^2+Vb^2);

Mat = det*[Va Vb; Vb -Va];
Iab = Mat*[2*p;2*q];

Iaaux = Iab(1);
Ibaux = Iab(2);

ilim=1e3;

if(Iaaux>ilim)
    Iaaux=ilim;
end;
if(Iaaux<-ilim)
    Iaaux =-ilim;    
end;

if(isnan(Iaaux))
    Iaaux=0;
end;
%-----------------

if(Ibaux>ilim)
    Ibaux=ilim;
end;
if(Ibaux<-ilim)
    Ibaux =-ilim;    
end;

if(isnan(Ibaux))
    Ibaux=0;
end;
%-----------------

Ia = Iaaux;
Ib = Ibaux;
